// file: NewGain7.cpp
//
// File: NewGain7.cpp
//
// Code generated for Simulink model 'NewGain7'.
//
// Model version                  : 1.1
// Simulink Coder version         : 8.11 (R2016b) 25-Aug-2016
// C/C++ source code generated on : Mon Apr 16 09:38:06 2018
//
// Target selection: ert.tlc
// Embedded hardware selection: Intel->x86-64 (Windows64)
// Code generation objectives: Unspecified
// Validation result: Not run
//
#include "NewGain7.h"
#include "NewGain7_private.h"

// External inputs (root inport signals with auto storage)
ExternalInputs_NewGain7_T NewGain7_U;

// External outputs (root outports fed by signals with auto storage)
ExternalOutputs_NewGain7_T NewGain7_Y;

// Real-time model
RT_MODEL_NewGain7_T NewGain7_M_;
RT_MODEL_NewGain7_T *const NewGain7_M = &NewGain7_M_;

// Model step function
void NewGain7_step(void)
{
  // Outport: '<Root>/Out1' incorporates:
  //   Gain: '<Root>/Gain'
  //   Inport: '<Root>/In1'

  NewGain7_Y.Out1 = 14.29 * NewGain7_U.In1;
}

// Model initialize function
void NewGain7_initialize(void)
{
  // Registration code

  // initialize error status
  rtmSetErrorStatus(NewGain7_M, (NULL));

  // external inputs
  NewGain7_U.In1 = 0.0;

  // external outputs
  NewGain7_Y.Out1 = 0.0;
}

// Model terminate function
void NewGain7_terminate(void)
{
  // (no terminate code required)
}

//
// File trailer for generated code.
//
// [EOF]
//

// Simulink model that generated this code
simulink model "NewGain7"  (R2016b)
settings: Solver=FixedStepAuto  StartTime=0.0  StopTime=10.0  RelTol=1e-3

== system NewGain7 ==
  In1 : Inport
  Gain : Gain  Gain=14.29
  Out1 : Outport
  wires:
  In1/1 -> Gain/1
  Gain/1 -> Out1/1
